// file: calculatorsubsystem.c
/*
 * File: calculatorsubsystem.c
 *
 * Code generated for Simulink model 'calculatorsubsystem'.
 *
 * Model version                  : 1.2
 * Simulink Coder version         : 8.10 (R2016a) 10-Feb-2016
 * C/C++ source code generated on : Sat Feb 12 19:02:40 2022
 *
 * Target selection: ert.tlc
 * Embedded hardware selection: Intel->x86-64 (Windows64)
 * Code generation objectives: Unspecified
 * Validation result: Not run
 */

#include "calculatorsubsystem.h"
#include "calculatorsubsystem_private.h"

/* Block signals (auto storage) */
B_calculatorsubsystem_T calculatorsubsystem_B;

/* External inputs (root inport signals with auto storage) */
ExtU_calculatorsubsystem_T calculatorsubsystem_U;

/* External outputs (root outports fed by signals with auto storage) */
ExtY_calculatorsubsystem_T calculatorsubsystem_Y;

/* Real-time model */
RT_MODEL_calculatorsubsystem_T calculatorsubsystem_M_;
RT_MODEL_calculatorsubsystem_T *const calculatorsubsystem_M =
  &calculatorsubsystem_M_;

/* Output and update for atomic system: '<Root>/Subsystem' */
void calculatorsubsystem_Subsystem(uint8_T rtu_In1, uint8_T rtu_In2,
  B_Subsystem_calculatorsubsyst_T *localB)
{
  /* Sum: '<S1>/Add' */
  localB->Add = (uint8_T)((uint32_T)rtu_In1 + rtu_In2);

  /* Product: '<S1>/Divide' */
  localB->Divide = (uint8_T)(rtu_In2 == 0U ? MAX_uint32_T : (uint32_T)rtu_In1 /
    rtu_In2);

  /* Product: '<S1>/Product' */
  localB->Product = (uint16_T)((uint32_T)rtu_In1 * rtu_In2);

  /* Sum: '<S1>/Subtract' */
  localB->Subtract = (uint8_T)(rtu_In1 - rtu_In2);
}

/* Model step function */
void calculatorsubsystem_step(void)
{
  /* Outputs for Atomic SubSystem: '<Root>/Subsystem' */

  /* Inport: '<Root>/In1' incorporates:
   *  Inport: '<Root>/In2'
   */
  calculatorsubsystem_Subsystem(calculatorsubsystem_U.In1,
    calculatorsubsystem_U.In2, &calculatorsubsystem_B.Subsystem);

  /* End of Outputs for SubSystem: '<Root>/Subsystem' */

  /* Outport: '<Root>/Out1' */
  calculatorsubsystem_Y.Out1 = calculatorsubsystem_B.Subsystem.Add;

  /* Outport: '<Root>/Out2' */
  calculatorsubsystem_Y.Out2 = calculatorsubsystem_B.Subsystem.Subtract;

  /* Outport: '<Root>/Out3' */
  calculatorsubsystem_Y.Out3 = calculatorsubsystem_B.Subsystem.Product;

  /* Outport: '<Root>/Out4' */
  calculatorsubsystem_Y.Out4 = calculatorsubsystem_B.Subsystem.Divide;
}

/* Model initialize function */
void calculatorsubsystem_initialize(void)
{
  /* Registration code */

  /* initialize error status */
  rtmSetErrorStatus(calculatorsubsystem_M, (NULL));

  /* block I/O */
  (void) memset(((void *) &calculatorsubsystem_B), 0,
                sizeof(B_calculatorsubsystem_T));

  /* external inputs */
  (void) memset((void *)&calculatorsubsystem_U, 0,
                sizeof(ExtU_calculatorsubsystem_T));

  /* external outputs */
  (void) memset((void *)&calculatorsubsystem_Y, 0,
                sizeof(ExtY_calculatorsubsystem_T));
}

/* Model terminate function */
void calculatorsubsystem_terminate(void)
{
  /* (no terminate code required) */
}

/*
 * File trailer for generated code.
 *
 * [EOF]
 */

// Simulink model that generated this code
simulink model "calculatorsubsystem"  (R2016a)
settings: Solver=FixedStepDiscrete  StartTime=0.0  StopTime=10.0  RelTol=1e-3

== system calculatorsubsystem ==
  In1 : Inport
  In2 : Inport  Port=2
  Subsystem : Subsystem  TreatAsAtomicUnit=on
  Out1 : Outport
  Out2 : Outport  Port=2
  Out3 : Outport  Port=3
  Out4 : Outport  Port=4
  wires:
  In2/1 -> Subsystem/2(In2)
  In1/1 -> Subsystem/1(In1)
  Subsystem/4(Out4) -> Out4/1
  Subsystem/3(Out3) -> Out3/1
  Subsystem/2(Out2) -> Out2/1
  Subsystem/1(Out1) -> Out1/1

== system calculatorsubsystem/Subsystem ==
  In1 : Inport  OutDataTypeStr=uint8
  In2 : Inport  Port=2  OutDataTypeStr=uint8
  Add : Sum
  Divide : Product  Inputs=*/
  Product : Product
  Subtract : Sum  Inputs=+-
  Out1 : Outport
  Out2 : Outport  Port=2
  Out3 : Outport  Port=3
  Out4 : Outport  Port=4
  wires:
  Add/1 -> Out1/1
  Subtract/1 -> Out2/1
  Product/1 -> Out3/1
  Divide/1 -> Out4/1
  In1/1 -> Divide/1, Subtract/1, Add/1, Product/1
  In2/1 -> Divide/2, Subtract/2, Add/2, Product/2
